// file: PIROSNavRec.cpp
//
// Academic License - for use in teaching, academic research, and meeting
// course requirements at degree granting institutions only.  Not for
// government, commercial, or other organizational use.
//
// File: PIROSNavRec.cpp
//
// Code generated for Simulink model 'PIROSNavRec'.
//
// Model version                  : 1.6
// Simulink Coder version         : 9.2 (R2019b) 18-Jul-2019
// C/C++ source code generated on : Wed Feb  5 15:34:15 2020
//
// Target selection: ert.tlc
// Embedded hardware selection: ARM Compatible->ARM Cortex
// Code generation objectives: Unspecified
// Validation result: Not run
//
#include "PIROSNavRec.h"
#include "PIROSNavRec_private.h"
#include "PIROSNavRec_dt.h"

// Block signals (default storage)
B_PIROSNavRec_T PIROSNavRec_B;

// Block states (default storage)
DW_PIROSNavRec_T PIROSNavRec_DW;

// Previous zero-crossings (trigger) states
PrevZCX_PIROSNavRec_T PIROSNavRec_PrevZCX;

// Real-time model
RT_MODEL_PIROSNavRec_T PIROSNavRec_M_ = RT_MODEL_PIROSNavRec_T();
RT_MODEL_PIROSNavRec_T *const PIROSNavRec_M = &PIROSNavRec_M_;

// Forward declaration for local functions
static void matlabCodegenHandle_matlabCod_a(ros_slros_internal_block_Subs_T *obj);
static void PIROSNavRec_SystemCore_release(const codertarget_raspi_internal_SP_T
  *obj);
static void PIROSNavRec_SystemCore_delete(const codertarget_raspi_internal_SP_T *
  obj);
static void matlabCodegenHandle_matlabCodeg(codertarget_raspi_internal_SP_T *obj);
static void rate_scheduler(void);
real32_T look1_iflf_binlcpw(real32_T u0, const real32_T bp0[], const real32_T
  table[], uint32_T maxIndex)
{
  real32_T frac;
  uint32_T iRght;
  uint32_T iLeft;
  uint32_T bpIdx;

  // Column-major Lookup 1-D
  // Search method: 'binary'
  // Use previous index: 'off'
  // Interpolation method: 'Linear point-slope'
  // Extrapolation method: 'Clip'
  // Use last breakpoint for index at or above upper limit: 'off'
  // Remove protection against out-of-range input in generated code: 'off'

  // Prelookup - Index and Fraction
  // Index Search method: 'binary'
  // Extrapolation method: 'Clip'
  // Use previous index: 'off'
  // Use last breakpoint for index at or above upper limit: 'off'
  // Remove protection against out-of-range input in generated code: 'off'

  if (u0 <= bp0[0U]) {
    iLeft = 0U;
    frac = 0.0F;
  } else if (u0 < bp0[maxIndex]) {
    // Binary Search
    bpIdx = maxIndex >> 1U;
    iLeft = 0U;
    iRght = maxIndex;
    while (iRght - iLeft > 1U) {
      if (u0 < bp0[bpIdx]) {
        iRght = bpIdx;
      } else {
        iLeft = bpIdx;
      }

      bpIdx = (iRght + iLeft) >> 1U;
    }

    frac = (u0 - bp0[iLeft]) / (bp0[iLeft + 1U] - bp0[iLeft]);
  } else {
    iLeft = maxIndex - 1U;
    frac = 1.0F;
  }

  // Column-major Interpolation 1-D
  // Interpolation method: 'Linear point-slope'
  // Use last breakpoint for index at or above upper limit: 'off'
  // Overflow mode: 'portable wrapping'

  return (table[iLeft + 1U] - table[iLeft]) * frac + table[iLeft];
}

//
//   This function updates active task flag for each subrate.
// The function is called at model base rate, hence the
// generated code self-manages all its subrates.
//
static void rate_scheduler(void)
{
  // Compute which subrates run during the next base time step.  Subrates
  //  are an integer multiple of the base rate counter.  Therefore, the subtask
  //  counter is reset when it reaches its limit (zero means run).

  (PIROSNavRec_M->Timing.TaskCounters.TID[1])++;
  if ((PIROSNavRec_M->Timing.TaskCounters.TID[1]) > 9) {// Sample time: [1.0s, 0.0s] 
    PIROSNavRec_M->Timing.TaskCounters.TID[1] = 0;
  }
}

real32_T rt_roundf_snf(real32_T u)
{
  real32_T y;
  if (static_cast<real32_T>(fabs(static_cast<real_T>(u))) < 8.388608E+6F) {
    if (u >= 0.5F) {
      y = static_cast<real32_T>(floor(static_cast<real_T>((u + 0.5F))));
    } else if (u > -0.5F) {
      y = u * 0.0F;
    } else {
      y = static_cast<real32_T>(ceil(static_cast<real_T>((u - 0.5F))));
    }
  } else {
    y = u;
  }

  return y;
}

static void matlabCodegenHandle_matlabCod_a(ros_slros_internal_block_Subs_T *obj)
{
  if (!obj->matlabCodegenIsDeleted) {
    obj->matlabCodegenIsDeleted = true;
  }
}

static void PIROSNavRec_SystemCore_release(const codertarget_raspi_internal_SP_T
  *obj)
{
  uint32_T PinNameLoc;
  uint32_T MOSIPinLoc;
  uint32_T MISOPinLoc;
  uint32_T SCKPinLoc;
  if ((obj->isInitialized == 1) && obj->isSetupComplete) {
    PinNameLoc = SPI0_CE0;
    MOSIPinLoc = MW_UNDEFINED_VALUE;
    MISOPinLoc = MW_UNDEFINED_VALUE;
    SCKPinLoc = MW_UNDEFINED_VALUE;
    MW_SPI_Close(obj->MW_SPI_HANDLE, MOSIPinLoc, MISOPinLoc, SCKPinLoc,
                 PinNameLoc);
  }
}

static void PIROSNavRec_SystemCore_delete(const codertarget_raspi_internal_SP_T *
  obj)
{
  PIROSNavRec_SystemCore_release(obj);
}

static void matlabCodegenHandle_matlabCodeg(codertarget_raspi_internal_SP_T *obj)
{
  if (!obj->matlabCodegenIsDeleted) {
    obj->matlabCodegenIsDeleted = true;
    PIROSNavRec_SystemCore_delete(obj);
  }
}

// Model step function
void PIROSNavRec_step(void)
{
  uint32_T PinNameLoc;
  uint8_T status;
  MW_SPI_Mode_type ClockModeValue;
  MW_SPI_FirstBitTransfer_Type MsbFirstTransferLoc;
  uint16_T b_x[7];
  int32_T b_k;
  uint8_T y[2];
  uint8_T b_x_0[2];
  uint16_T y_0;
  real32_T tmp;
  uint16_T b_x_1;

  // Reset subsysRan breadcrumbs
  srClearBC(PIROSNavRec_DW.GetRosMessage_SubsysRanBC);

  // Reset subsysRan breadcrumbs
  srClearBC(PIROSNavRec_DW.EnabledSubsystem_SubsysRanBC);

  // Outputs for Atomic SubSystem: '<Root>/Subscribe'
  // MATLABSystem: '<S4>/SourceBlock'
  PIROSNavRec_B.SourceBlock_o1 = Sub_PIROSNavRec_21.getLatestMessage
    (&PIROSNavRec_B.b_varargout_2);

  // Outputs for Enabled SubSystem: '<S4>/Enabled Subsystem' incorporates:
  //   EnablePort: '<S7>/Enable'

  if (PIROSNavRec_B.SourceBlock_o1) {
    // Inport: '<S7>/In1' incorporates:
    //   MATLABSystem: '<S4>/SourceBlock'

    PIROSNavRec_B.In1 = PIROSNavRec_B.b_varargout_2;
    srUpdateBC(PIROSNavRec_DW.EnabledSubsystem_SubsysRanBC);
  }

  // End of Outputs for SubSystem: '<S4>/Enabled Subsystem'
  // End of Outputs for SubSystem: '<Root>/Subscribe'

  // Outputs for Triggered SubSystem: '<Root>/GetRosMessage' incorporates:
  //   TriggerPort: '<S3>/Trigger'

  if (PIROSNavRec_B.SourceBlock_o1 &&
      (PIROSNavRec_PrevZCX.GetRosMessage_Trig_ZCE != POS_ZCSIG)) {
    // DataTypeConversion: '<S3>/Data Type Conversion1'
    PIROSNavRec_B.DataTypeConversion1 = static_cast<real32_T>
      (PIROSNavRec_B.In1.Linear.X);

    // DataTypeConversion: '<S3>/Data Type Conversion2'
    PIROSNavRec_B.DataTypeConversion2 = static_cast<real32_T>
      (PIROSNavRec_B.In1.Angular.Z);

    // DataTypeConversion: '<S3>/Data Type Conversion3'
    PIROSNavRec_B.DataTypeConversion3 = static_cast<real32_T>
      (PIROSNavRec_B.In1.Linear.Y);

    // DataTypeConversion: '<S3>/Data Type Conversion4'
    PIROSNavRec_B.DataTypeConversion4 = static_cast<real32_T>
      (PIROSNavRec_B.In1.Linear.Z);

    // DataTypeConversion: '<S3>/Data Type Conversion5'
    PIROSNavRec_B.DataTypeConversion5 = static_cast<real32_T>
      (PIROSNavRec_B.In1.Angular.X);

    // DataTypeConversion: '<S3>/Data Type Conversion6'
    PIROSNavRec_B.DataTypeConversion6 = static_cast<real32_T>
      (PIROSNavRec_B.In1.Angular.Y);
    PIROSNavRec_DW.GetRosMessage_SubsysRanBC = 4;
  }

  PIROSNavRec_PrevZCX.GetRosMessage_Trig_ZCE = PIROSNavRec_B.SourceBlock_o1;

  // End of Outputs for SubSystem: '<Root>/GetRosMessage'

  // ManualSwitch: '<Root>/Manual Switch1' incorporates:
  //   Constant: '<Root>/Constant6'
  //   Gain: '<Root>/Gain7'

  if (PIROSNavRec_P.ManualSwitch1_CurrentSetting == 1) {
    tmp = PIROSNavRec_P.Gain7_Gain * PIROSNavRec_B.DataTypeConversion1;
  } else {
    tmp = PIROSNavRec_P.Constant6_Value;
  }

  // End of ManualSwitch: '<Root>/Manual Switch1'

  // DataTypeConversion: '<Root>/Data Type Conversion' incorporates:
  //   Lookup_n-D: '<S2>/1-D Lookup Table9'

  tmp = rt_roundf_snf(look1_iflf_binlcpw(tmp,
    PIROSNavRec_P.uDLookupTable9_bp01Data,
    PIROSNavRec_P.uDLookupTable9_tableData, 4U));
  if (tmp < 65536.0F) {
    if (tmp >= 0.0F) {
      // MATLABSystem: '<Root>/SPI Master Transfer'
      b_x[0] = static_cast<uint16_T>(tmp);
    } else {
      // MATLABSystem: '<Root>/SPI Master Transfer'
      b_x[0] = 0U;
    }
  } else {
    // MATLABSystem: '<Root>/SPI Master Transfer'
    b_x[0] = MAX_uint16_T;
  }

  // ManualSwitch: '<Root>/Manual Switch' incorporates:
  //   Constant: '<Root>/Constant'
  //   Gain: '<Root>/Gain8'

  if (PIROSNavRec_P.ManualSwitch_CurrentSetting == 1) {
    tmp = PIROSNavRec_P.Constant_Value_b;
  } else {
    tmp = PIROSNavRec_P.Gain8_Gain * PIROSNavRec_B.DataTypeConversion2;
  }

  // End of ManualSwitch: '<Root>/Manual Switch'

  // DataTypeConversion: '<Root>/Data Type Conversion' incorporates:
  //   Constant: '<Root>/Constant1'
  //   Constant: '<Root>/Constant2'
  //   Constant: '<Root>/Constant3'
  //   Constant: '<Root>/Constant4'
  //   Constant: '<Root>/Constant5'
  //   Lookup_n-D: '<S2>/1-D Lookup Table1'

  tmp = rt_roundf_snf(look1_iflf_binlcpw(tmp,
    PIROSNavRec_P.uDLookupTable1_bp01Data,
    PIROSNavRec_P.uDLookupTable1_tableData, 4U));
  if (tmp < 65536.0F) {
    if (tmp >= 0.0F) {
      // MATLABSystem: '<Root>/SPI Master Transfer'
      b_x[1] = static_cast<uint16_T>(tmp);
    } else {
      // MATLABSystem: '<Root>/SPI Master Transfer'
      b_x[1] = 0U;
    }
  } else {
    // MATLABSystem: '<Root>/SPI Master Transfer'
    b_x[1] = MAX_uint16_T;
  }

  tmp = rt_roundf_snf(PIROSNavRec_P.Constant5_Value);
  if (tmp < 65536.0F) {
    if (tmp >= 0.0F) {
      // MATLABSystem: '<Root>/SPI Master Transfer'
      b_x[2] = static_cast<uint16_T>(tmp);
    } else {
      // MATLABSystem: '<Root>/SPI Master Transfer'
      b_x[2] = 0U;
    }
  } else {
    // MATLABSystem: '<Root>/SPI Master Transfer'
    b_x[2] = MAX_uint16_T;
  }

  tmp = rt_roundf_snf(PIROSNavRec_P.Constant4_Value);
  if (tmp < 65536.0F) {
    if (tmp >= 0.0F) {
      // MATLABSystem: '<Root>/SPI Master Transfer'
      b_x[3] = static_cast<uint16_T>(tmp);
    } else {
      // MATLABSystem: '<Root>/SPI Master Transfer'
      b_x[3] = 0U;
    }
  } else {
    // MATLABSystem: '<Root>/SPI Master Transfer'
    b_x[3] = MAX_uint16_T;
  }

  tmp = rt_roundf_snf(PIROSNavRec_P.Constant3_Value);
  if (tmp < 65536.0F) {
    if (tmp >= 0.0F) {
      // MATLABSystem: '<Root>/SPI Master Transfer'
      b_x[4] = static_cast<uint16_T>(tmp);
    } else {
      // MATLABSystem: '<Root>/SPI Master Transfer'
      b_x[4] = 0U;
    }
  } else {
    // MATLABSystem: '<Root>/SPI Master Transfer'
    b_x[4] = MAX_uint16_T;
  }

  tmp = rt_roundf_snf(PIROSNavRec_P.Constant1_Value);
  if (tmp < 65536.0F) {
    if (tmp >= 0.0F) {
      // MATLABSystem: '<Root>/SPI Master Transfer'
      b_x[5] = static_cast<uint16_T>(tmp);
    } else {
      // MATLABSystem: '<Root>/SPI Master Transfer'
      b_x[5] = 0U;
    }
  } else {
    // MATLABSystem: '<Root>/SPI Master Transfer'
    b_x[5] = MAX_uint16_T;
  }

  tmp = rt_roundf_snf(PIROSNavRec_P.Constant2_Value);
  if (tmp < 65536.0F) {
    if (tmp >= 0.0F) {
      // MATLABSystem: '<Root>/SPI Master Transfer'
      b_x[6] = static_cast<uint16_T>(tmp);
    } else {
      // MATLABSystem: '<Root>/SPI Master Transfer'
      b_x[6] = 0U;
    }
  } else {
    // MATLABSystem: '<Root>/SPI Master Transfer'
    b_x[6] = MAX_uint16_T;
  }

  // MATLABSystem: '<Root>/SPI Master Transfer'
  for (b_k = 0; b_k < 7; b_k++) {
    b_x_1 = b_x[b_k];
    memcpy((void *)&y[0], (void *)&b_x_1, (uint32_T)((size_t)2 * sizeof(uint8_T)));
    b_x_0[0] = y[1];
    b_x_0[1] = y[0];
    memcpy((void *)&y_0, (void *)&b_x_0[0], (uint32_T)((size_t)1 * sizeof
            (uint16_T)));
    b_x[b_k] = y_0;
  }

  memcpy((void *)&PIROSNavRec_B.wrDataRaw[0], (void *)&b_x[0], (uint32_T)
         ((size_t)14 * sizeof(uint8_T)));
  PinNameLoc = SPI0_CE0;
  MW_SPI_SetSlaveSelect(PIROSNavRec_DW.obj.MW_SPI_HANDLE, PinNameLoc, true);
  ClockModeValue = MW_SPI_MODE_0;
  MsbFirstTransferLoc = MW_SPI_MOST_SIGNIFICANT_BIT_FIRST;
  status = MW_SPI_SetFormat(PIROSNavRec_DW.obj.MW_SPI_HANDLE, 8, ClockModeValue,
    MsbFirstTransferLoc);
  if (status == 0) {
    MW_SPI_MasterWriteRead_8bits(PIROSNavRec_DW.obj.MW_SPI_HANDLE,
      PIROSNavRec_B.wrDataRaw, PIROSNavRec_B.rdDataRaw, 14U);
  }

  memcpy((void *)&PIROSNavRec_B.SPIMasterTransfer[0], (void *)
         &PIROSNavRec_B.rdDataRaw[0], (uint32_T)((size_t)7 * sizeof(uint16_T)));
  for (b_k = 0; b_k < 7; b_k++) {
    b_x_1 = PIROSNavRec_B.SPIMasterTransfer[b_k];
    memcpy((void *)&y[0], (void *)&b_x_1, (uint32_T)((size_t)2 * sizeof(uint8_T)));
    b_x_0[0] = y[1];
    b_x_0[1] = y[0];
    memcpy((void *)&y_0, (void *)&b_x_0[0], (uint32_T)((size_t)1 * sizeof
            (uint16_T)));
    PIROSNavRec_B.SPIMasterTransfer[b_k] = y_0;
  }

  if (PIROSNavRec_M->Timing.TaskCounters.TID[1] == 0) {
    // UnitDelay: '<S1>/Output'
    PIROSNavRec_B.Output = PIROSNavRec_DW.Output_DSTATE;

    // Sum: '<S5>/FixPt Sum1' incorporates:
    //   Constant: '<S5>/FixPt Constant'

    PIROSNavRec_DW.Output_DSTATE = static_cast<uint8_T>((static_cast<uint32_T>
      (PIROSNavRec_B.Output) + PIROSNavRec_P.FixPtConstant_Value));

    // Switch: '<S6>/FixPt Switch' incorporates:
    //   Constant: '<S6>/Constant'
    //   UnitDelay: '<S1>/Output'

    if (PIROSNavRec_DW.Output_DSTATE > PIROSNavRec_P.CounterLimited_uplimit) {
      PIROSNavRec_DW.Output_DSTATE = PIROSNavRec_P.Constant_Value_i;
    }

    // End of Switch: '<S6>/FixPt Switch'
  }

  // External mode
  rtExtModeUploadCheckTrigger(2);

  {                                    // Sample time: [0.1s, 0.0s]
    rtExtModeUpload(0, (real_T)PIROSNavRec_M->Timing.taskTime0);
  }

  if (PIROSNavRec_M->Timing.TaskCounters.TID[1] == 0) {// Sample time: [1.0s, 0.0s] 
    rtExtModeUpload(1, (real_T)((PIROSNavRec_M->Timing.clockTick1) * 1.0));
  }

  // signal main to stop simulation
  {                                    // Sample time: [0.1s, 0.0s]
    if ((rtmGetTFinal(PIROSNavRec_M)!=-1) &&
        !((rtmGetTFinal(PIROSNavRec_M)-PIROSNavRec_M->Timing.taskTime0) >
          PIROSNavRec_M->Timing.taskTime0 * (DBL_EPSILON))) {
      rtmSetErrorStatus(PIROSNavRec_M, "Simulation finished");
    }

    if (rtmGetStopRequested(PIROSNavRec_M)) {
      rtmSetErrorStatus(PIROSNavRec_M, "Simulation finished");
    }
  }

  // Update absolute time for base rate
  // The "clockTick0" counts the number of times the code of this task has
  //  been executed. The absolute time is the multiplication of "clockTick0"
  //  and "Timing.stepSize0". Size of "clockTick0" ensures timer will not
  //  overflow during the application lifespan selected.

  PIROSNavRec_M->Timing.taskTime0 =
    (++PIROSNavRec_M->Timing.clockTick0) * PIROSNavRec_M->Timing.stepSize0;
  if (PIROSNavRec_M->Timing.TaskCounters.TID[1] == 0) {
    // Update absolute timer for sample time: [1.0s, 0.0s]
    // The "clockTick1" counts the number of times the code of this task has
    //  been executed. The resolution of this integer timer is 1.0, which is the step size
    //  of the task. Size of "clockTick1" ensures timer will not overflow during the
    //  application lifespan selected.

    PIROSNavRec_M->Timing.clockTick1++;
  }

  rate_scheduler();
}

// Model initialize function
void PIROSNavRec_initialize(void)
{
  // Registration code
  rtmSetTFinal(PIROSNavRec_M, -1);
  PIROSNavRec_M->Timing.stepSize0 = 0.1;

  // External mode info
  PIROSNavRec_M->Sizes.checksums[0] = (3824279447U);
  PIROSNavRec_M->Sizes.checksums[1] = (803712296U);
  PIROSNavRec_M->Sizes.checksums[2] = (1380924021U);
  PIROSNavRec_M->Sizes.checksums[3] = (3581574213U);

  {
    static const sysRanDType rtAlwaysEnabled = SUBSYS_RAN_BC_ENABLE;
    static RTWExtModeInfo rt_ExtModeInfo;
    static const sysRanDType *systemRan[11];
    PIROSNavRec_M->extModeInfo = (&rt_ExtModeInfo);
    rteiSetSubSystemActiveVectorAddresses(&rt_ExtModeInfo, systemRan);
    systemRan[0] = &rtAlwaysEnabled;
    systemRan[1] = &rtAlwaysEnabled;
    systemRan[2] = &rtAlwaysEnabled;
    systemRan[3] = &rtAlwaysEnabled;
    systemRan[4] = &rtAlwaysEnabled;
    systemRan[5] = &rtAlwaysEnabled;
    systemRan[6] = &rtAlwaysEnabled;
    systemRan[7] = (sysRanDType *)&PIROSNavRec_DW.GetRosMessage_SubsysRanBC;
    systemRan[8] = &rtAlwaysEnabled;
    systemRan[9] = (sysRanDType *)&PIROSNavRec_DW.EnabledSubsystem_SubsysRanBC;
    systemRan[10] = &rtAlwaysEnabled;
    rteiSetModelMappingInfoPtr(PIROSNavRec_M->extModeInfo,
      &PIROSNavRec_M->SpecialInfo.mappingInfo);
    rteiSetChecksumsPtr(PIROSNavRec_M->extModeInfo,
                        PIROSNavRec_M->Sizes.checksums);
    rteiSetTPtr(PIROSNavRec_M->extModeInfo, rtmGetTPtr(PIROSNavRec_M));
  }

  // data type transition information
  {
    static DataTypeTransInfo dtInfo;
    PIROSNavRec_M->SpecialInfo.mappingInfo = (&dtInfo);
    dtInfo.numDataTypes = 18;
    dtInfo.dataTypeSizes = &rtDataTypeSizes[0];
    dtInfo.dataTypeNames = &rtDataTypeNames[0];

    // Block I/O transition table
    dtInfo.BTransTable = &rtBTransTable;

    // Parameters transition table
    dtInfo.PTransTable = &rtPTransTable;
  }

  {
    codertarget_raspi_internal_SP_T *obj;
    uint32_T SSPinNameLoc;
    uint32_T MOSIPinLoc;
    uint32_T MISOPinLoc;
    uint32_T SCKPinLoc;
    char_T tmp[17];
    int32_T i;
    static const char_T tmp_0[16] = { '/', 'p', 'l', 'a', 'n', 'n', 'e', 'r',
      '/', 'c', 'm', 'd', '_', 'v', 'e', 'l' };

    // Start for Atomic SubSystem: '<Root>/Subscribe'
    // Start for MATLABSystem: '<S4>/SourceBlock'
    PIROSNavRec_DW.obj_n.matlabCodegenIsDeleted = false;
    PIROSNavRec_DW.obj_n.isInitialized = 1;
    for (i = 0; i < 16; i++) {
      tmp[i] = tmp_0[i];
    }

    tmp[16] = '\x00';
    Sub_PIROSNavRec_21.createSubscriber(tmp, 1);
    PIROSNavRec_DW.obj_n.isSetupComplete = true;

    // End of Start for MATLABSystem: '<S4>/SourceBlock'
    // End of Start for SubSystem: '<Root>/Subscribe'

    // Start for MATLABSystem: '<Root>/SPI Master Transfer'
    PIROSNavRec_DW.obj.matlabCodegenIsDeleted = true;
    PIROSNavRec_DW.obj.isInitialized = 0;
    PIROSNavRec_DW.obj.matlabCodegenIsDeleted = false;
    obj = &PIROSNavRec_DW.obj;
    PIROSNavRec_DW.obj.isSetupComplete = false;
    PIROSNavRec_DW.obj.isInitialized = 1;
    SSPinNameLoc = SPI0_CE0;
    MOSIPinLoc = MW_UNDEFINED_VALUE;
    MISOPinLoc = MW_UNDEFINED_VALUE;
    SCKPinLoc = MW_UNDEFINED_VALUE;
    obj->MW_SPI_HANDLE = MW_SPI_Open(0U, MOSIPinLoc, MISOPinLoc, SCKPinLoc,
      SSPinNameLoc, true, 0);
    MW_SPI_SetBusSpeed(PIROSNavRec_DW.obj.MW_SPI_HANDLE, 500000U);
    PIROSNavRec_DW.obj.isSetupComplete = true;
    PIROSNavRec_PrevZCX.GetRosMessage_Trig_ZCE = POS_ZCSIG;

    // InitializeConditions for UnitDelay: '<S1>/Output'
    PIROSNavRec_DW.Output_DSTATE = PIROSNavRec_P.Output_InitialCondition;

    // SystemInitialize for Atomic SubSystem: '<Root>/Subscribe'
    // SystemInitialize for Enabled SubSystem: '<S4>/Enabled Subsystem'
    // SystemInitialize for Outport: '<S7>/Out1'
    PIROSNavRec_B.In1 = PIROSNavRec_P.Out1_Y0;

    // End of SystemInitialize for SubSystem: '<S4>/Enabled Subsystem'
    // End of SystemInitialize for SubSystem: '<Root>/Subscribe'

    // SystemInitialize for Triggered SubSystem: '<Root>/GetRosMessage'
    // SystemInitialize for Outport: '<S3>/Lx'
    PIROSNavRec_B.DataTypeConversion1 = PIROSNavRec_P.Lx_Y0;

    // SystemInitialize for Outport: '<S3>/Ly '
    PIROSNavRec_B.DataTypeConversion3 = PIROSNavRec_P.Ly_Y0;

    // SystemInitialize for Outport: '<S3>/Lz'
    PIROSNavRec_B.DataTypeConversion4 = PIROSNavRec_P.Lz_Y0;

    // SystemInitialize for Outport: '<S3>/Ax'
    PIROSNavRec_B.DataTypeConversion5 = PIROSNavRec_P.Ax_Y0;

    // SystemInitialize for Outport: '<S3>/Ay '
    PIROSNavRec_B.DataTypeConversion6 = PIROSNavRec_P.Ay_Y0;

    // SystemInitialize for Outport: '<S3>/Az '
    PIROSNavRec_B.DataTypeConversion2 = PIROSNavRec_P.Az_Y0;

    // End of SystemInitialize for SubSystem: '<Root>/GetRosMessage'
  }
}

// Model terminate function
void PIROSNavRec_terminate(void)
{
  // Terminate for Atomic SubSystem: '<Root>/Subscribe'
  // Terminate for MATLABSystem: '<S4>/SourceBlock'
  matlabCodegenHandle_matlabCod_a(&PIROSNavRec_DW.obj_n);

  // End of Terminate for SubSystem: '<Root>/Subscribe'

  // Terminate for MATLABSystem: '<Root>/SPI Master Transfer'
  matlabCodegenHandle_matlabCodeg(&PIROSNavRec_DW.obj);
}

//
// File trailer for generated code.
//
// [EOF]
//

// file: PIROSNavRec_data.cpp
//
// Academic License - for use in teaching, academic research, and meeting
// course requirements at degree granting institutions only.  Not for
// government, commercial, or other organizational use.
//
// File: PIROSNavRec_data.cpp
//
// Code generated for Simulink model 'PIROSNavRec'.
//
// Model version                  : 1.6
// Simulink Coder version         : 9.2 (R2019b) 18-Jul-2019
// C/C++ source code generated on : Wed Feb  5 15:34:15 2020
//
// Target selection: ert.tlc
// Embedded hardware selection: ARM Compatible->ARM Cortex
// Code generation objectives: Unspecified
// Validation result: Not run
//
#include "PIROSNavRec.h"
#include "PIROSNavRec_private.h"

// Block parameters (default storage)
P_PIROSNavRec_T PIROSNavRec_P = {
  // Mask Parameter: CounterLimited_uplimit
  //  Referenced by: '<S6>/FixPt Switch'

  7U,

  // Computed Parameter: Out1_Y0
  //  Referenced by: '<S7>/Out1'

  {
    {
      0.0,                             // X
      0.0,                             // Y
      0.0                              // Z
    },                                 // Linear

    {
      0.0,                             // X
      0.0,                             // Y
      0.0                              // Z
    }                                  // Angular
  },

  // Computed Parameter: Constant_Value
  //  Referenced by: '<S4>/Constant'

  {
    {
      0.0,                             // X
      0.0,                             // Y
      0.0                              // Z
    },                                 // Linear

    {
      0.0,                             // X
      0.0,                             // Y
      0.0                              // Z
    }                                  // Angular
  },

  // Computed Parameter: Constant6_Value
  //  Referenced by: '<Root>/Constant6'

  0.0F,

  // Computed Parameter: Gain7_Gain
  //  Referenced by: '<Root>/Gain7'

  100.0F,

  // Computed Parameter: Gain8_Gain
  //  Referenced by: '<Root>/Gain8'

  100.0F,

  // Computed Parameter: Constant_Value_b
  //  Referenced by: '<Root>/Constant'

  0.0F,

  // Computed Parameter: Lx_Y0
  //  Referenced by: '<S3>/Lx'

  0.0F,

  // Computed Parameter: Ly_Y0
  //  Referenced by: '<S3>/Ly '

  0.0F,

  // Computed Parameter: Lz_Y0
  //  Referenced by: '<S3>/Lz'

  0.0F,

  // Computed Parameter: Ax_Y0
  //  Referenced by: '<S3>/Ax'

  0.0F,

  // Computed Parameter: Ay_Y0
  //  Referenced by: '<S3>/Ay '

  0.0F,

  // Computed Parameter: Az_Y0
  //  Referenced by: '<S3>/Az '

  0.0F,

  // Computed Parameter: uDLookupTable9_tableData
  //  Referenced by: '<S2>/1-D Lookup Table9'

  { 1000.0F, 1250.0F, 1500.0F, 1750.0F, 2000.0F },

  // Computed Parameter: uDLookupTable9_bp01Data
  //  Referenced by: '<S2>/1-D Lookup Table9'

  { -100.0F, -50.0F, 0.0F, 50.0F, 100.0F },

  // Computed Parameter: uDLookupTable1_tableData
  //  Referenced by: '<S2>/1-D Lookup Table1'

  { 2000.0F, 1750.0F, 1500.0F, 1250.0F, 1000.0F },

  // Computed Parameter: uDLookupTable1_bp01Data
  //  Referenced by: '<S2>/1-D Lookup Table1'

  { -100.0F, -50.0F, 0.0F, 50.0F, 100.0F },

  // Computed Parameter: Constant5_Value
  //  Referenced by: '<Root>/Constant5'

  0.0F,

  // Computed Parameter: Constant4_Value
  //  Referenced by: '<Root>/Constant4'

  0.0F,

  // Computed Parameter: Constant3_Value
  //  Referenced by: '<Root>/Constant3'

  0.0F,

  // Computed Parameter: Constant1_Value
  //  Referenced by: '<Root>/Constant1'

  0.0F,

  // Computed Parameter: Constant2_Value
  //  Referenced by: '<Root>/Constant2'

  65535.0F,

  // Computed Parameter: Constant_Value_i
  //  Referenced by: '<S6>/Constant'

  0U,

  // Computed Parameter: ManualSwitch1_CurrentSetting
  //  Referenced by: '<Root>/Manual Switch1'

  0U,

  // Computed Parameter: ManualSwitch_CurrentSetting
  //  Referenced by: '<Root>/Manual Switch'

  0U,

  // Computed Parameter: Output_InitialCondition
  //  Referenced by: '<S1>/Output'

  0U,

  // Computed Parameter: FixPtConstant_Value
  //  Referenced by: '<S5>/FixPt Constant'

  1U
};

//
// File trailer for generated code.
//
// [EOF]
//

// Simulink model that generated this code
simulink model "PIROSNavRec"  (Simulink 10.0)
settings: Solver=FixedStepAuto  StartTime=0.0  StopTime=inf  RelTol=1e-3
libraries: simulink x1, raspberrypilib x1, robotlib x1

== system PIROSNavRec ==
  note: Counter to show Pi is functiuoning when runniong in external mode
  Constant{,1,3..6} (6 alike) : Constant  Value=0  OutDataTypeStr=single
  Constant2 : Constant  Value=65535  OutDataTypeStr=single
  Counter Limited : simulink/Sources/Counter Limited  uplimit=7  tsamp=1
  Data Type Conversion : DataTypeConversion  OutDataTypeStr=uint16  RndMeth=Round  SaturateOnIntegerOverflow=on
  Display{,1..2,15} (4 alike) : Display
  ForwardBack_LeftRight : Subsystem
  Gain7 : Gain  Gain=100
  Gain8 : Gain  Gain=100
  GetRosMessage : Subsystem
  Manual Switch : ManualSwitch  CurrentSetting=0
  Manual Switch1 : ManualSwitch  CurrentSetting=0
  Mux : Mux  Inputs=7
  Mux1 : Mux  Inputs=6
  Rate Transition1 : RateTransition  OutPortSampleTime=0.1
  SPI Master Transfer : raspberrypilib/SPI Master Transfer  BoardProperty=Pi 3 Model B+  SPIModule=uint32(0)  Mode=Master  BusSpeed=1000000  Pin=SPI0_CE0  FirstBitToTransfer=Most significant bit (MSB)  ClockMode=0  BlockFunction=Transfer  RegisterAddress=0  OutputDataType=int8  OutputDataLength=1
  Subscribe : robotlib/Subscribe  topicSource=Select from ROS network  topic=/planner/cmd_vel  messageType=geometry_msgs/Twist  sampleTime=0.1  messageQueueLength=1
  Terminator{2..5} (4 alike) : Terminator
  wires:
  GetRosMessage/4(Ax) -> Mux1/4, Terminator4/1
  Subscribe/1 -> Display1/1, GetRosMessage/Trigger
  GetRosMessage/3(Lz) -> Mux1/3, Terminator3/1
  GetRosMessage/2("Ly ") -> Mux1/2, Terminator2/1
  Mux1/1 -> Display/1
  GetRosMessage/5("Ay ") -> Mux1/5, Terminator5/1
  Subscribe/2 -> GetRosMessage/1(In1)
  GetRosMessage/1(Lx) -> Gain7/1, Mux1/1  "Forward_Back"
  Gain8/1 -> Manual Switch/2
  GetRosMessage/6("Az ") -> Mux1/6, Gain8/1  "Left_right"
  Gain7/1 -> Manual Switch1/1
  Constant2/1 -> Mux/7
  ForwardBack_LeftRight/2(LeftRight) -> Mux/2
  ForwardBack_LeftRight/1(ForwardsBack) -> Mux/1
  Constant1/1 -> Mux/6
  Constant3/1 -> Mux/5
  Constant4/1 -> Mux/4
  Constant5/1 -> Mux/3
  SPI Master Transfer/1 -> Display2/1
  Data Type Conversion/1 -> Rate Transition1/1
  Mux/1 -> Data Type Conversion/1
  Rate Transition1/1 -> SPI Master Transfer/1
  Counter Limited/1 -> Display15/1
  Constant/1 -> Manual Switch/1
  Manual Switch/1 -> ForwardBack_LeftRight/1(In2)
  Constant6/1 -> Manual Switch1/2
  Manual Switch1/1 -> ForwardBack_LeftRight/2(In1)

== system PIROSNavRec/ForwardBack_LeftRight ==
  note: input a -100 to 100 value for reverse and forwards. -100 is 100% speed backwards 100 is 100%speed forwards
  note: input a -100 to 100 value for left and right. -100 is 100% speed left 100 is 100%speed right
  In2 : Inport
  In1 : Inport  Port=2
  1-D Lookup Table1 : Lookup_n-D  NumberOfTableDimensions=1  BreakpointsForDimension1=[-100,-50,0,50,100]  BreakpointsForDimension1FirstPoint=0  BreakpointsForDimension1Spacing=1.8  Table=[2000;1750;1500;1250;1000]  ExtrapMethod=Clip  InternalRulePriority=Speed  RndMeth=Simplest  InputSameDT=on
  1-D Lookup Table9 : Lookup_n-D  NumberOfTableDimensions=1  BreakpointsForDimension1=[-100,-50,0,50,100]  BreakpointsForDimension1FirstPoint=0  BreakpointsForDimension1Spacing=1.8  Table=[1000;1250;1500;1750;2000]  ExtrapMethod=Clip  InternalRulePriority=Speed  RndMeth=Simplest  InputSameDT=on
  ForwardsBack : Outport
  LeftRight : Outport  Port=2
  wires:
  In1/1 -> 1-D Lookup Table9/1
  1-D Lookup Table1/1 -> LeftRight/1  "Up_Down"
  1-D Lookup Table9/1 -> ForwardsBack/1  "Left_right"
  In2/1 -> 1-D Lookup Table1/1

== system PIROSNavRec/GetRosMessage ==
  note: Linear Commands
  note: AngularCommands
  In1 : Inport
  Trigger : TriggerPort  VariantControl=Variant  PortDimensions=1
  Bus Selector : BusSelector  OutputSignals=Linear.X,Linear.Y,Linear.Z,Angular.X,Angular.Y,Angular.Z
  Data Type Conversion{1..6} (6 alike) : DataTypeConversion  OutDataTypeStr=single
  Lx : Outport  OutDataTypeStr=single
  "Ly " : Outport  Port=2
  Lz : Outport  Port=3
  Ax : Outport  Port=4
  "Ay " : Outport  Port=5
  "Az " : Outport  Port=6  OutDataTypeStr=single
  wires:
  Bus Selector/2 -> Data Type Conversion3/1  "<Y>"
  Bus Selector/1 -> Data Type Conversion1/1  "<X>"
  In1/1 -> Bus Selector/1
  Bus Selector/3 -> Data Type Conversion4/1  "<Z>"
  Bus Selector/4 -> Data Type Conversion5/1  "<X>"
  Bus Selector/5 -> Data Type Conversion6/1  "<Y>"
  Bus Selector/6 -> Data Type Conversion2/1  "<Z>"
  Data Type Conversion1/1 -> Lx/1
  Data Type Conversion2/1 -> "Az "/1
  Data Type Conversion3/1 -> "Ly "/1
  Data Type Conversion4/1 -> Lz/1
  Data Type Conversion5/1 -> Ax/1
  Data Type Conversion6/1 -> "Ay "/1
